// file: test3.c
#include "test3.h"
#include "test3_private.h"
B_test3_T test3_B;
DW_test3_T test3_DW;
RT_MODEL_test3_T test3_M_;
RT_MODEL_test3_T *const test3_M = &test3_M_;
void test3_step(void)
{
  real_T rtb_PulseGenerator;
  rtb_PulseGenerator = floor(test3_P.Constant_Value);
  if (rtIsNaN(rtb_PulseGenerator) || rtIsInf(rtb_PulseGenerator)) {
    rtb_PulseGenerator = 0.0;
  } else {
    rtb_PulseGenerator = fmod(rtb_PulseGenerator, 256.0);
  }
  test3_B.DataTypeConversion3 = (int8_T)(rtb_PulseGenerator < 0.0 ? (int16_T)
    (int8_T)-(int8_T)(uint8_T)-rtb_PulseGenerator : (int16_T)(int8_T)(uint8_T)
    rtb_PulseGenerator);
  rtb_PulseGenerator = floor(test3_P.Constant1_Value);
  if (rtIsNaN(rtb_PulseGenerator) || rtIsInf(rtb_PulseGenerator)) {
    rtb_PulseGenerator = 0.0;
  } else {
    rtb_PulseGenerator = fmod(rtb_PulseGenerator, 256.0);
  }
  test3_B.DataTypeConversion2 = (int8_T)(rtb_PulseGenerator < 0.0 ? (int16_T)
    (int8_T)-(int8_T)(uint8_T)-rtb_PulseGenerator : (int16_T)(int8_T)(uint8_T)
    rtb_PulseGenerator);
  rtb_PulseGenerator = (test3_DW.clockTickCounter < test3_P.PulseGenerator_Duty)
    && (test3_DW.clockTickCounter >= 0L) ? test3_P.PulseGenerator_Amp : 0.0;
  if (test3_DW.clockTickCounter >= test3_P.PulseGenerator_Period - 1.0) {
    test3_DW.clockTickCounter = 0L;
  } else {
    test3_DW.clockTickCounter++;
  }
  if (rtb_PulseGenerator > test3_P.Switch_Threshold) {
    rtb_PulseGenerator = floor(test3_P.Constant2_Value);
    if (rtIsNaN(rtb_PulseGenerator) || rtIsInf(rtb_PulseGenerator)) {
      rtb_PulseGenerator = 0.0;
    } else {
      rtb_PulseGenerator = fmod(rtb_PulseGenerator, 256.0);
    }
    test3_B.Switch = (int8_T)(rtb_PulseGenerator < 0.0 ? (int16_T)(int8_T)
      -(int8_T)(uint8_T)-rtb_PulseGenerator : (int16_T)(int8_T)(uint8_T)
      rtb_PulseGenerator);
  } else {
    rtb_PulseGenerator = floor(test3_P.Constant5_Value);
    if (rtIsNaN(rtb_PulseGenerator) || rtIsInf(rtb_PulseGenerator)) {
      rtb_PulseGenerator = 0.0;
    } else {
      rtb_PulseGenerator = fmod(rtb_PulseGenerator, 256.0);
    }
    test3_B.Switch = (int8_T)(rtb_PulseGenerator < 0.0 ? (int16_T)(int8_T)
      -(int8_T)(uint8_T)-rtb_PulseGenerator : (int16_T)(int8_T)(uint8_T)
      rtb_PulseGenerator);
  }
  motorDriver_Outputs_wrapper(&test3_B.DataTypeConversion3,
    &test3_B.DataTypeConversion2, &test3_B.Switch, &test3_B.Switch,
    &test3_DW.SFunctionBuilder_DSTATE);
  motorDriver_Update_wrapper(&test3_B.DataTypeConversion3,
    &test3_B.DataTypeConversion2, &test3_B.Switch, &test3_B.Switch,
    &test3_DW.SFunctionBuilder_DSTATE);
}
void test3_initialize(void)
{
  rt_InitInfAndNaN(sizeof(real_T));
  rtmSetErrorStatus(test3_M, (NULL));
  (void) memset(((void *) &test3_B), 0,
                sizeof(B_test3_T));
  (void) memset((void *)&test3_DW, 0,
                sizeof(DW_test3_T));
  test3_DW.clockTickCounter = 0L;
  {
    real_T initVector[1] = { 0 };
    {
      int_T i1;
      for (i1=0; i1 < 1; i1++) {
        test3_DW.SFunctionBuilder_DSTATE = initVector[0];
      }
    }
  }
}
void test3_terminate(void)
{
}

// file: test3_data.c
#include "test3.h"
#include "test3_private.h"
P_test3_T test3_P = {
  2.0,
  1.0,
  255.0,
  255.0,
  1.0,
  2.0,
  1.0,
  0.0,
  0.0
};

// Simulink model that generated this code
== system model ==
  SFunctionBuilder : S-Function  FunctionName=motorDriver  <- 1: DataTypeConversion3, 2: DataTypeConversion2, 3: Switch, 4: Switch
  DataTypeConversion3 : DataTypeConversion  <- 1: Constant
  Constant : Constant  Value=255
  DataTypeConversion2 : DataTypeConversion  <- 1: Constant1
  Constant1 : Constant  Value=255
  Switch : Switch  Criteria=u2 > Threshold  <- 1: DataTypeConversion#1, 2: PulseGenerator, 3: DataTypeConversion#2
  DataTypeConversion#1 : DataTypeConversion  <- 1: Constant2
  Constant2 : Constant
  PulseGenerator : DiscretePulseGenerator  Period=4  PulseWidth=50
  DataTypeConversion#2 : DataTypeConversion  <- 1: Constant5
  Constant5 : Constant  Value=2
